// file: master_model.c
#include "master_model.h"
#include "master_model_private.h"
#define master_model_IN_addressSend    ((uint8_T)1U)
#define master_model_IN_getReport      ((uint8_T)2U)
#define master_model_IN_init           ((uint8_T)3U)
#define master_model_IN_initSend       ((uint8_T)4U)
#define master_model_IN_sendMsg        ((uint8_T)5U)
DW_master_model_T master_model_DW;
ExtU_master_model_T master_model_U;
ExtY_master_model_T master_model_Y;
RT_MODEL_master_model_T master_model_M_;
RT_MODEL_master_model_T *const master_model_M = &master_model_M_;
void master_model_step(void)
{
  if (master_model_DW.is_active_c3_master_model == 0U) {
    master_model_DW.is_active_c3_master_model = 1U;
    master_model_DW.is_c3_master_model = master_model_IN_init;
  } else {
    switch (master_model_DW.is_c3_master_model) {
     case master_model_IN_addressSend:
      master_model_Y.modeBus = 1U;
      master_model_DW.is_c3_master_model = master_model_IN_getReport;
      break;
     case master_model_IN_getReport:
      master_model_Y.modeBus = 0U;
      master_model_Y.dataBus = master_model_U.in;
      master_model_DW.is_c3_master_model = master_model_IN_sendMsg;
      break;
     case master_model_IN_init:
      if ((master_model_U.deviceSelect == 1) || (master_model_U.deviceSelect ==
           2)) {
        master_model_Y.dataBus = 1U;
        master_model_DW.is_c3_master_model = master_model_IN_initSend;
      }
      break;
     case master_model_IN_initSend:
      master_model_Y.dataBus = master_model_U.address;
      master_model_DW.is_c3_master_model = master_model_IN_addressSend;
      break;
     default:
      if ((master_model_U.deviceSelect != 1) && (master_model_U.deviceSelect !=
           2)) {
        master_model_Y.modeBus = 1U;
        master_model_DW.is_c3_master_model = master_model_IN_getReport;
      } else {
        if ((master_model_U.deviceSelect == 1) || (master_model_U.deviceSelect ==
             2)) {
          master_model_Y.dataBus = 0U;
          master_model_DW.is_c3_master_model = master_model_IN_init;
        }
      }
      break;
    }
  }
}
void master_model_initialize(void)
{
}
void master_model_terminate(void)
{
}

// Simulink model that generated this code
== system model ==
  deviceSelect : Inport
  in : Inport
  address : Inport
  modeBus : Outport  <- 1: Stateflowchart#1
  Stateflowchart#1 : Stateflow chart  <- 1: deviceSelect, 2: in, 3: address
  dataBus : Outport  <- 1: Stateflowchart#1/2
== stateflow chart Stateflowchart#1 ==
  state init
  state initSend
  state addressSend
  state sendMsg
  state getReport
  (default) -> init
  init -> initSend : [deviceSelect==1 || deviceSelect==2]{dataBus=1}
  initSend -> addressSend : {dataBus=address}
  sendMsg -> init [order 2] : [deviceSelect==1 || deviceSelect==2]{dataBus=0}
  addressSend -> getReport : {modeBus=1}
  getReport -> sendMsg : {modeBus=0; dataBus=in}
  sendMsg -> getReport [order 1] : [deviceSelect ~=1 && deviceSelect~=2]{modeBus=1}
  data: modeBus output uint8; dataBus output uint8; deviceSelect input uint8; in input uint8; address input uint8
